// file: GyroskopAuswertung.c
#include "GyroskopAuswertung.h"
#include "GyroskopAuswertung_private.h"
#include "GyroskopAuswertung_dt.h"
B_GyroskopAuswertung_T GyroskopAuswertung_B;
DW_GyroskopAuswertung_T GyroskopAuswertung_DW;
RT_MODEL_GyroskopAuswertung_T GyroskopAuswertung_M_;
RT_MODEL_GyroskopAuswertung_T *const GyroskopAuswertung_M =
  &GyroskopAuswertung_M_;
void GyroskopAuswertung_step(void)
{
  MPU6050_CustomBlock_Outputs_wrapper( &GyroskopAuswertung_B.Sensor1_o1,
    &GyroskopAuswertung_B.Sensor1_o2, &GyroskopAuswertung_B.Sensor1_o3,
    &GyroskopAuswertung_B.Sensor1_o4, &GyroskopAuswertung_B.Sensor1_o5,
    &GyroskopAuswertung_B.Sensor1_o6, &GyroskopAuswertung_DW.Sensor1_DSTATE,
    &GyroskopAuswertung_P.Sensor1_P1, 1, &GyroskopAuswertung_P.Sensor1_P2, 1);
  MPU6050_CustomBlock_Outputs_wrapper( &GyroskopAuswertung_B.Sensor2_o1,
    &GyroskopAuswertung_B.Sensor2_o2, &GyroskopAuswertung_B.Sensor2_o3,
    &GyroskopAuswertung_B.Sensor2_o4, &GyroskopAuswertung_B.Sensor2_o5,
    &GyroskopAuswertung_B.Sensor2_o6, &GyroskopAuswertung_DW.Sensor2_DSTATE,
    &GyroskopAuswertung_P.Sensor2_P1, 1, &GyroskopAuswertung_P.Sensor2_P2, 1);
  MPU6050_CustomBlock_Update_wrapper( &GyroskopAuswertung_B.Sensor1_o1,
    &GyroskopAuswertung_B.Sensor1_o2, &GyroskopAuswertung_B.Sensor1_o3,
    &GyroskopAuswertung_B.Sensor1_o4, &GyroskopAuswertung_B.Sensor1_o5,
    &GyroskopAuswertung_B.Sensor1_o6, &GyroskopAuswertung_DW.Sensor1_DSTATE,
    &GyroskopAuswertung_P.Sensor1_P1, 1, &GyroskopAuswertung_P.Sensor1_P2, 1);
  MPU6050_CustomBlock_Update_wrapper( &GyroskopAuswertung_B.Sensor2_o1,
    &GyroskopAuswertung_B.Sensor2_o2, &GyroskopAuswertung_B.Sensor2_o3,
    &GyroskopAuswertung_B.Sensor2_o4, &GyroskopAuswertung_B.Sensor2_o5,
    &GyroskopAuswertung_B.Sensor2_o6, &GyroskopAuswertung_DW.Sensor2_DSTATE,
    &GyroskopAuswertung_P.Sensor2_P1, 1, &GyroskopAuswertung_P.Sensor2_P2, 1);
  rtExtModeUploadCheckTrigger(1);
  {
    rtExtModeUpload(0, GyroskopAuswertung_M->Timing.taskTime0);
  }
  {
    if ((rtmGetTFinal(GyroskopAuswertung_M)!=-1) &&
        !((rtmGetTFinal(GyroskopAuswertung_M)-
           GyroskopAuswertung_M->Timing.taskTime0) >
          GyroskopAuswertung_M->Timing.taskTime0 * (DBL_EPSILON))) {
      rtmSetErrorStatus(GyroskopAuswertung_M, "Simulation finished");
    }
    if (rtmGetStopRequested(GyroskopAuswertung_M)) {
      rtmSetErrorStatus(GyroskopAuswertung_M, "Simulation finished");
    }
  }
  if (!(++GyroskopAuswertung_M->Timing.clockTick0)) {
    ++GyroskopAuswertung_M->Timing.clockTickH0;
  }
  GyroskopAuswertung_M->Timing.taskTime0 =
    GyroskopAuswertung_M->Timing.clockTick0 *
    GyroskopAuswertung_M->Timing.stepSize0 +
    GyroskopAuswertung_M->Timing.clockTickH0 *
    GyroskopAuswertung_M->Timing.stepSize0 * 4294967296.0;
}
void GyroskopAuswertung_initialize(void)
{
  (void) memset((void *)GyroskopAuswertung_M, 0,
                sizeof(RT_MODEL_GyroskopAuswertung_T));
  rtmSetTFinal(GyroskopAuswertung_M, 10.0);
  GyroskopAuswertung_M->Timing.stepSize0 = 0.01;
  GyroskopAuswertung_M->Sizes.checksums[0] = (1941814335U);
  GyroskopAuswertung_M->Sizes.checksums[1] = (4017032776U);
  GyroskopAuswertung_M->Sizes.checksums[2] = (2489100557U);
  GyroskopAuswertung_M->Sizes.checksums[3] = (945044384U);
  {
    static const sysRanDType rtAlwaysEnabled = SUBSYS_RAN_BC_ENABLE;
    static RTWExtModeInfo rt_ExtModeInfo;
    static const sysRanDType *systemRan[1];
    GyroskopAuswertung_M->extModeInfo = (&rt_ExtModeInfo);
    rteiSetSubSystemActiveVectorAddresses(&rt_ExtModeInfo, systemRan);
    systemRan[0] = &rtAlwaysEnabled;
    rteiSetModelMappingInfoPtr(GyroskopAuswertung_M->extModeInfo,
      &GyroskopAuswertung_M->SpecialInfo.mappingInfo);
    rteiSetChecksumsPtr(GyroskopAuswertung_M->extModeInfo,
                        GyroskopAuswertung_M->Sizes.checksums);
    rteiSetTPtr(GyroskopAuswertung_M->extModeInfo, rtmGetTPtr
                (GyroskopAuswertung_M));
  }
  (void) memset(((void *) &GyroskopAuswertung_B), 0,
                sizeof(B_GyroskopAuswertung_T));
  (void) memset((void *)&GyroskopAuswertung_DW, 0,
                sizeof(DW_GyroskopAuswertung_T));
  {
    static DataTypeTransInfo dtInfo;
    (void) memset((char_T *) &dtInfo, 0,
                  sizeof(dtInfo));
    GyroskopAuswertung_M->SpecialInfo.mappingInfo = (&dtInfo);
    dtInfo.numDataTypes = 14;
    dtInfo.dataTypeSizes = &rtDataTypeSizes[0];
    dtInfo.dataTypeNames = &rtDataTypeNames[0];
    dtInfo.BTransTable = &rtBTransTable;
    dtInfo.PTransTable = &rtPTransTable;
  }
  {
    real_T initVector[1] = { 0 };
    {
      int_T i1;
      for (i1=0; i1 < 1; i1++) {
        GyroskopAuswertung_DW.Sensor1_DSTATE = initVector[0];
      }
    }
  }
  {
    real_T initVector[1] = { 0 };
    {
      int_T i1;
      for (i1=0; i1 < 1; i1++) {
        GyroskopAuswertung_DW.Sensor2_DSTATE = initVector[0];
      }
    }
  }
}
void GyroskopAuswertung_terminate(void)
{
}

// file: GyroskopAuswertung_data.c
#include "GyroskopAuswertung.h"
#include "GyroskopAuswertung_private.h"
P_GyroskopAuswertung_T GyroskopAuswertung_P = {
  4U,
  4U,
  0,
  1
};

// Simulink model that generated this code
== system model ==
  Sensor1 : S-Function  FunctionName=MPU6050_CustomBlock
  Sensor2 : S-Function  FunctionName=MPU6050_CustomBlock
